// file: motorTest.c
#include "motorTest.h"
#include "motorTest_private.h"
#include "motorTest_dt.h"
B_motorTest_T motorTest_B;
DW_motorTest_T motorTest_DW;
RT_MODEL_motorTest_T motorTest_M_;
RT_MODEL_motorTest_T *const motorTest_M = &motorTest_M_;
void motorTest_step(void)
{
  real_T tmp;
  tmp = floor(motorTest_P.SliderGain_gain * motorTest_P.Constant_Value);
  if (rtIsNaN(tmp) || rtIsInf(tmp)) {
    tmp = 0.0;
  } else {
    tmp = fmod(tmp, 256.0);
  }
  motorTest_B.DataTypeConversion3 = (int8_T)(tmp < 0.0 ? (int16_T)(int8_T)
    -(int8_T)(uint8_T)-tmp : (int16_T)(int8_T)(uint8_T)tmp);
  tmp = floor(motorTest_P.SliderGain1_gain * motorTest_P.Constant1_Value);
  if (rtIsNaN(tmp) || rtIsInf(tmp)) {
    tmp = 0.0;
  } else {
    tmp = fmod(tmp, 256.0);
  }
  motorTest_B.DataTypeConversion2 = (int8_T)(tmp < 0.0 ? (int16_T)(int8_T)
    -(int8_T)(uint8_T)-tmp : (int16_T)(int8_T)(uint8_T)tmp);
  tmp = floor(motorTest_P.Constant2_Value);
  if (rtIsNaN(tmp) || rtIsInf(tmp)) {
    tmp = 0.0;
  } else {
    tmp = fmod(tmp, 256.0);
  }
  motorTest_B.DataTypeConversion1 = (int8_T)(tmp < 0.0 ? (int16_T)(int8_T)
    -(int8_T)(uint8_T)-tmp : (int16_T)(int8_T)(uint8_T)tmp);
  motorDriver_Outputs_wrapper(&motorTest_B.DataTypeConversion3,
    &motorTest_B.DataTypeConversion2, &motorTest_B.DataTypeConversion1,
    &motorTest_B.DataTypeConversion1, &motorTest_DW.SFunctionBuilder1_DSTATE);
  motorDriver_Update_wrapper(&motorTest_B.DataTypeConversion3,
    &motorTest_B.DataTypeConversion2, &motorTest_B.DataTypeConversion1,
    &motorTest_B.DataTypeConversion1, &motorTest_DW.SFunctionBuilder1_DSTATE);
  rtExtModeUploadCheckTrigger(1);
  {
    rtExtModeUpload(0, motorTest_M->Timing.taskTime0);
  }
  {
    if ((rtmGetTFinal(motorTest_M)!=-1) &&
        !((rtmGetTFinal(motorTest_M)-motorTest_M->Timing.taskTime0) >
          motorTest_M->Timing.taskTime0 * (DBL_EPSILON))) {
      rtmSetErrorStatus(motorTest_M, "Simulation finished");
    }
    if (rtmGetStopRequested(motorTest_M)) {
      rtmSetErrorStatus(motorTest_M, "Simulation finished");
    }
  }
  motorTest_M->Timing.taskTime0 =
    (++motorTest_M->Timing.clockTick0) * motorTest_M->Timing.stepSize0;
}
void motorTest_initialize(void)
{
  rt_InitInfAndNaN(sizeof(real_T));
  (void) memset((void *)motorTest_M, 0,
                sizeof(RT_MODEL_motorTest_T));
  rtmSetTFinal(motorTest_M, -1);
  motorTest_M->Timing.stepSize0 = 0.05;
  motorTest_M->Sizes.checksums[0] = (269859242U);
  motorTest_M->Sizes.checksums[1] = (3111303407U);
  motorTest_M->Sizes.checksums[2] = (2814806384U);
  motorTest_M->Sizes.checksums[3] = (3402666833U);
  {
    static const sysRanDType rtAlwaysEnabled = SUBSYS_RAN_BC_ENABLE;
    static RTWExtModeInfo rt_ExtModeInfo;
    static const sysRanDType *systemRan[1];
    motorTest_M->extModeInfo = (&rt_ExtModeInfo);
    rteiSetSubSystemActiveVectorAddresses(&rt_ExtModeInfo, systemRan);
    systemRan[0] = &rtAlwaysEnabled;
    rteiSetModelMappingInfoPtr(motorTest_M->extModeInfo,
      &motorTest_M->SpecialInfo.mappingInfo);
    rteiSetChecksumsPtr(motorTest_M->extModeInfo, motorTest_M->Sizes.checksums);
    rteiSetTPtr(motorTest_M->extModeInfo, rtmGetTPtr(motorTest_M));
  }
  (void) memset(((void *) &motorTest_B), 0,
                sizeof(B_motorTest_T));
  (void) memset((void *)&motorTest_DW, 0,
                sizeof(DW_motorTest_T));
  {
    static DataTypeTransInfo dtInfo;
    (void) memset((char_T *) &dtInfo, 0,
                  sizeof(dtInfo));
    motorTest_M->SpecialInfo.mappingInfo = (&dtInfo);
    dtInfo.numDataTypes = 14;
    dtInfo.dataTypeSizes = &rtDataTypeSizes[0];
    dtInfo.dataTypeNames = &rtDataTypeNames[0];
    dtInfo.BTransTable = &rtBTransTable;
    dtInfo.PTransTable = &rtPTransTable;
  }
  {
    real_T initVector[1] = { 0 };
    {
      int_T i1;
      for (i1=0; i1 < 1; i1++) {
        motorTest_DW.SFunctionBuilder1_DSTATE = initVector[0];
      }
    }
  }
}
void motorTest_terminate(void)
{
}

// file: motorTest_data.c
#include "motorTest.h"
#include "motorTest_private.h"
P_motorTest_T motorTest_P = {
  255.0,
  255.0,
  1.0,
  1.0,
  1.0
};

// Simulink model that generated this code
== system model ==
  SFunctionBuilder1 : S-Function  FunctionName=motorDriver  <- 1: DataTypeConversion3, 2: DataTypeConversion2, 3: DataTypeConversion1, 4: DataTypeConversion1
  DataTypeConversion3 : DataTypeConversion  <- 1: SliderGain
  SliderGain : simulink/Math Operations/Slider Gain  <- 1: Constant
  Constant : Constant
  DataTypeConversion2 : DataTypeConversion  <- 1: SliderGain1
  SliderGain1 : simulink/Math Operations/Slider Gain  <- 1: Constant1
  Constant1 : Constant
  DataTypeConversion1 : DataTypeConversion  <- 1: Constant2
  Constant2 : Constant
